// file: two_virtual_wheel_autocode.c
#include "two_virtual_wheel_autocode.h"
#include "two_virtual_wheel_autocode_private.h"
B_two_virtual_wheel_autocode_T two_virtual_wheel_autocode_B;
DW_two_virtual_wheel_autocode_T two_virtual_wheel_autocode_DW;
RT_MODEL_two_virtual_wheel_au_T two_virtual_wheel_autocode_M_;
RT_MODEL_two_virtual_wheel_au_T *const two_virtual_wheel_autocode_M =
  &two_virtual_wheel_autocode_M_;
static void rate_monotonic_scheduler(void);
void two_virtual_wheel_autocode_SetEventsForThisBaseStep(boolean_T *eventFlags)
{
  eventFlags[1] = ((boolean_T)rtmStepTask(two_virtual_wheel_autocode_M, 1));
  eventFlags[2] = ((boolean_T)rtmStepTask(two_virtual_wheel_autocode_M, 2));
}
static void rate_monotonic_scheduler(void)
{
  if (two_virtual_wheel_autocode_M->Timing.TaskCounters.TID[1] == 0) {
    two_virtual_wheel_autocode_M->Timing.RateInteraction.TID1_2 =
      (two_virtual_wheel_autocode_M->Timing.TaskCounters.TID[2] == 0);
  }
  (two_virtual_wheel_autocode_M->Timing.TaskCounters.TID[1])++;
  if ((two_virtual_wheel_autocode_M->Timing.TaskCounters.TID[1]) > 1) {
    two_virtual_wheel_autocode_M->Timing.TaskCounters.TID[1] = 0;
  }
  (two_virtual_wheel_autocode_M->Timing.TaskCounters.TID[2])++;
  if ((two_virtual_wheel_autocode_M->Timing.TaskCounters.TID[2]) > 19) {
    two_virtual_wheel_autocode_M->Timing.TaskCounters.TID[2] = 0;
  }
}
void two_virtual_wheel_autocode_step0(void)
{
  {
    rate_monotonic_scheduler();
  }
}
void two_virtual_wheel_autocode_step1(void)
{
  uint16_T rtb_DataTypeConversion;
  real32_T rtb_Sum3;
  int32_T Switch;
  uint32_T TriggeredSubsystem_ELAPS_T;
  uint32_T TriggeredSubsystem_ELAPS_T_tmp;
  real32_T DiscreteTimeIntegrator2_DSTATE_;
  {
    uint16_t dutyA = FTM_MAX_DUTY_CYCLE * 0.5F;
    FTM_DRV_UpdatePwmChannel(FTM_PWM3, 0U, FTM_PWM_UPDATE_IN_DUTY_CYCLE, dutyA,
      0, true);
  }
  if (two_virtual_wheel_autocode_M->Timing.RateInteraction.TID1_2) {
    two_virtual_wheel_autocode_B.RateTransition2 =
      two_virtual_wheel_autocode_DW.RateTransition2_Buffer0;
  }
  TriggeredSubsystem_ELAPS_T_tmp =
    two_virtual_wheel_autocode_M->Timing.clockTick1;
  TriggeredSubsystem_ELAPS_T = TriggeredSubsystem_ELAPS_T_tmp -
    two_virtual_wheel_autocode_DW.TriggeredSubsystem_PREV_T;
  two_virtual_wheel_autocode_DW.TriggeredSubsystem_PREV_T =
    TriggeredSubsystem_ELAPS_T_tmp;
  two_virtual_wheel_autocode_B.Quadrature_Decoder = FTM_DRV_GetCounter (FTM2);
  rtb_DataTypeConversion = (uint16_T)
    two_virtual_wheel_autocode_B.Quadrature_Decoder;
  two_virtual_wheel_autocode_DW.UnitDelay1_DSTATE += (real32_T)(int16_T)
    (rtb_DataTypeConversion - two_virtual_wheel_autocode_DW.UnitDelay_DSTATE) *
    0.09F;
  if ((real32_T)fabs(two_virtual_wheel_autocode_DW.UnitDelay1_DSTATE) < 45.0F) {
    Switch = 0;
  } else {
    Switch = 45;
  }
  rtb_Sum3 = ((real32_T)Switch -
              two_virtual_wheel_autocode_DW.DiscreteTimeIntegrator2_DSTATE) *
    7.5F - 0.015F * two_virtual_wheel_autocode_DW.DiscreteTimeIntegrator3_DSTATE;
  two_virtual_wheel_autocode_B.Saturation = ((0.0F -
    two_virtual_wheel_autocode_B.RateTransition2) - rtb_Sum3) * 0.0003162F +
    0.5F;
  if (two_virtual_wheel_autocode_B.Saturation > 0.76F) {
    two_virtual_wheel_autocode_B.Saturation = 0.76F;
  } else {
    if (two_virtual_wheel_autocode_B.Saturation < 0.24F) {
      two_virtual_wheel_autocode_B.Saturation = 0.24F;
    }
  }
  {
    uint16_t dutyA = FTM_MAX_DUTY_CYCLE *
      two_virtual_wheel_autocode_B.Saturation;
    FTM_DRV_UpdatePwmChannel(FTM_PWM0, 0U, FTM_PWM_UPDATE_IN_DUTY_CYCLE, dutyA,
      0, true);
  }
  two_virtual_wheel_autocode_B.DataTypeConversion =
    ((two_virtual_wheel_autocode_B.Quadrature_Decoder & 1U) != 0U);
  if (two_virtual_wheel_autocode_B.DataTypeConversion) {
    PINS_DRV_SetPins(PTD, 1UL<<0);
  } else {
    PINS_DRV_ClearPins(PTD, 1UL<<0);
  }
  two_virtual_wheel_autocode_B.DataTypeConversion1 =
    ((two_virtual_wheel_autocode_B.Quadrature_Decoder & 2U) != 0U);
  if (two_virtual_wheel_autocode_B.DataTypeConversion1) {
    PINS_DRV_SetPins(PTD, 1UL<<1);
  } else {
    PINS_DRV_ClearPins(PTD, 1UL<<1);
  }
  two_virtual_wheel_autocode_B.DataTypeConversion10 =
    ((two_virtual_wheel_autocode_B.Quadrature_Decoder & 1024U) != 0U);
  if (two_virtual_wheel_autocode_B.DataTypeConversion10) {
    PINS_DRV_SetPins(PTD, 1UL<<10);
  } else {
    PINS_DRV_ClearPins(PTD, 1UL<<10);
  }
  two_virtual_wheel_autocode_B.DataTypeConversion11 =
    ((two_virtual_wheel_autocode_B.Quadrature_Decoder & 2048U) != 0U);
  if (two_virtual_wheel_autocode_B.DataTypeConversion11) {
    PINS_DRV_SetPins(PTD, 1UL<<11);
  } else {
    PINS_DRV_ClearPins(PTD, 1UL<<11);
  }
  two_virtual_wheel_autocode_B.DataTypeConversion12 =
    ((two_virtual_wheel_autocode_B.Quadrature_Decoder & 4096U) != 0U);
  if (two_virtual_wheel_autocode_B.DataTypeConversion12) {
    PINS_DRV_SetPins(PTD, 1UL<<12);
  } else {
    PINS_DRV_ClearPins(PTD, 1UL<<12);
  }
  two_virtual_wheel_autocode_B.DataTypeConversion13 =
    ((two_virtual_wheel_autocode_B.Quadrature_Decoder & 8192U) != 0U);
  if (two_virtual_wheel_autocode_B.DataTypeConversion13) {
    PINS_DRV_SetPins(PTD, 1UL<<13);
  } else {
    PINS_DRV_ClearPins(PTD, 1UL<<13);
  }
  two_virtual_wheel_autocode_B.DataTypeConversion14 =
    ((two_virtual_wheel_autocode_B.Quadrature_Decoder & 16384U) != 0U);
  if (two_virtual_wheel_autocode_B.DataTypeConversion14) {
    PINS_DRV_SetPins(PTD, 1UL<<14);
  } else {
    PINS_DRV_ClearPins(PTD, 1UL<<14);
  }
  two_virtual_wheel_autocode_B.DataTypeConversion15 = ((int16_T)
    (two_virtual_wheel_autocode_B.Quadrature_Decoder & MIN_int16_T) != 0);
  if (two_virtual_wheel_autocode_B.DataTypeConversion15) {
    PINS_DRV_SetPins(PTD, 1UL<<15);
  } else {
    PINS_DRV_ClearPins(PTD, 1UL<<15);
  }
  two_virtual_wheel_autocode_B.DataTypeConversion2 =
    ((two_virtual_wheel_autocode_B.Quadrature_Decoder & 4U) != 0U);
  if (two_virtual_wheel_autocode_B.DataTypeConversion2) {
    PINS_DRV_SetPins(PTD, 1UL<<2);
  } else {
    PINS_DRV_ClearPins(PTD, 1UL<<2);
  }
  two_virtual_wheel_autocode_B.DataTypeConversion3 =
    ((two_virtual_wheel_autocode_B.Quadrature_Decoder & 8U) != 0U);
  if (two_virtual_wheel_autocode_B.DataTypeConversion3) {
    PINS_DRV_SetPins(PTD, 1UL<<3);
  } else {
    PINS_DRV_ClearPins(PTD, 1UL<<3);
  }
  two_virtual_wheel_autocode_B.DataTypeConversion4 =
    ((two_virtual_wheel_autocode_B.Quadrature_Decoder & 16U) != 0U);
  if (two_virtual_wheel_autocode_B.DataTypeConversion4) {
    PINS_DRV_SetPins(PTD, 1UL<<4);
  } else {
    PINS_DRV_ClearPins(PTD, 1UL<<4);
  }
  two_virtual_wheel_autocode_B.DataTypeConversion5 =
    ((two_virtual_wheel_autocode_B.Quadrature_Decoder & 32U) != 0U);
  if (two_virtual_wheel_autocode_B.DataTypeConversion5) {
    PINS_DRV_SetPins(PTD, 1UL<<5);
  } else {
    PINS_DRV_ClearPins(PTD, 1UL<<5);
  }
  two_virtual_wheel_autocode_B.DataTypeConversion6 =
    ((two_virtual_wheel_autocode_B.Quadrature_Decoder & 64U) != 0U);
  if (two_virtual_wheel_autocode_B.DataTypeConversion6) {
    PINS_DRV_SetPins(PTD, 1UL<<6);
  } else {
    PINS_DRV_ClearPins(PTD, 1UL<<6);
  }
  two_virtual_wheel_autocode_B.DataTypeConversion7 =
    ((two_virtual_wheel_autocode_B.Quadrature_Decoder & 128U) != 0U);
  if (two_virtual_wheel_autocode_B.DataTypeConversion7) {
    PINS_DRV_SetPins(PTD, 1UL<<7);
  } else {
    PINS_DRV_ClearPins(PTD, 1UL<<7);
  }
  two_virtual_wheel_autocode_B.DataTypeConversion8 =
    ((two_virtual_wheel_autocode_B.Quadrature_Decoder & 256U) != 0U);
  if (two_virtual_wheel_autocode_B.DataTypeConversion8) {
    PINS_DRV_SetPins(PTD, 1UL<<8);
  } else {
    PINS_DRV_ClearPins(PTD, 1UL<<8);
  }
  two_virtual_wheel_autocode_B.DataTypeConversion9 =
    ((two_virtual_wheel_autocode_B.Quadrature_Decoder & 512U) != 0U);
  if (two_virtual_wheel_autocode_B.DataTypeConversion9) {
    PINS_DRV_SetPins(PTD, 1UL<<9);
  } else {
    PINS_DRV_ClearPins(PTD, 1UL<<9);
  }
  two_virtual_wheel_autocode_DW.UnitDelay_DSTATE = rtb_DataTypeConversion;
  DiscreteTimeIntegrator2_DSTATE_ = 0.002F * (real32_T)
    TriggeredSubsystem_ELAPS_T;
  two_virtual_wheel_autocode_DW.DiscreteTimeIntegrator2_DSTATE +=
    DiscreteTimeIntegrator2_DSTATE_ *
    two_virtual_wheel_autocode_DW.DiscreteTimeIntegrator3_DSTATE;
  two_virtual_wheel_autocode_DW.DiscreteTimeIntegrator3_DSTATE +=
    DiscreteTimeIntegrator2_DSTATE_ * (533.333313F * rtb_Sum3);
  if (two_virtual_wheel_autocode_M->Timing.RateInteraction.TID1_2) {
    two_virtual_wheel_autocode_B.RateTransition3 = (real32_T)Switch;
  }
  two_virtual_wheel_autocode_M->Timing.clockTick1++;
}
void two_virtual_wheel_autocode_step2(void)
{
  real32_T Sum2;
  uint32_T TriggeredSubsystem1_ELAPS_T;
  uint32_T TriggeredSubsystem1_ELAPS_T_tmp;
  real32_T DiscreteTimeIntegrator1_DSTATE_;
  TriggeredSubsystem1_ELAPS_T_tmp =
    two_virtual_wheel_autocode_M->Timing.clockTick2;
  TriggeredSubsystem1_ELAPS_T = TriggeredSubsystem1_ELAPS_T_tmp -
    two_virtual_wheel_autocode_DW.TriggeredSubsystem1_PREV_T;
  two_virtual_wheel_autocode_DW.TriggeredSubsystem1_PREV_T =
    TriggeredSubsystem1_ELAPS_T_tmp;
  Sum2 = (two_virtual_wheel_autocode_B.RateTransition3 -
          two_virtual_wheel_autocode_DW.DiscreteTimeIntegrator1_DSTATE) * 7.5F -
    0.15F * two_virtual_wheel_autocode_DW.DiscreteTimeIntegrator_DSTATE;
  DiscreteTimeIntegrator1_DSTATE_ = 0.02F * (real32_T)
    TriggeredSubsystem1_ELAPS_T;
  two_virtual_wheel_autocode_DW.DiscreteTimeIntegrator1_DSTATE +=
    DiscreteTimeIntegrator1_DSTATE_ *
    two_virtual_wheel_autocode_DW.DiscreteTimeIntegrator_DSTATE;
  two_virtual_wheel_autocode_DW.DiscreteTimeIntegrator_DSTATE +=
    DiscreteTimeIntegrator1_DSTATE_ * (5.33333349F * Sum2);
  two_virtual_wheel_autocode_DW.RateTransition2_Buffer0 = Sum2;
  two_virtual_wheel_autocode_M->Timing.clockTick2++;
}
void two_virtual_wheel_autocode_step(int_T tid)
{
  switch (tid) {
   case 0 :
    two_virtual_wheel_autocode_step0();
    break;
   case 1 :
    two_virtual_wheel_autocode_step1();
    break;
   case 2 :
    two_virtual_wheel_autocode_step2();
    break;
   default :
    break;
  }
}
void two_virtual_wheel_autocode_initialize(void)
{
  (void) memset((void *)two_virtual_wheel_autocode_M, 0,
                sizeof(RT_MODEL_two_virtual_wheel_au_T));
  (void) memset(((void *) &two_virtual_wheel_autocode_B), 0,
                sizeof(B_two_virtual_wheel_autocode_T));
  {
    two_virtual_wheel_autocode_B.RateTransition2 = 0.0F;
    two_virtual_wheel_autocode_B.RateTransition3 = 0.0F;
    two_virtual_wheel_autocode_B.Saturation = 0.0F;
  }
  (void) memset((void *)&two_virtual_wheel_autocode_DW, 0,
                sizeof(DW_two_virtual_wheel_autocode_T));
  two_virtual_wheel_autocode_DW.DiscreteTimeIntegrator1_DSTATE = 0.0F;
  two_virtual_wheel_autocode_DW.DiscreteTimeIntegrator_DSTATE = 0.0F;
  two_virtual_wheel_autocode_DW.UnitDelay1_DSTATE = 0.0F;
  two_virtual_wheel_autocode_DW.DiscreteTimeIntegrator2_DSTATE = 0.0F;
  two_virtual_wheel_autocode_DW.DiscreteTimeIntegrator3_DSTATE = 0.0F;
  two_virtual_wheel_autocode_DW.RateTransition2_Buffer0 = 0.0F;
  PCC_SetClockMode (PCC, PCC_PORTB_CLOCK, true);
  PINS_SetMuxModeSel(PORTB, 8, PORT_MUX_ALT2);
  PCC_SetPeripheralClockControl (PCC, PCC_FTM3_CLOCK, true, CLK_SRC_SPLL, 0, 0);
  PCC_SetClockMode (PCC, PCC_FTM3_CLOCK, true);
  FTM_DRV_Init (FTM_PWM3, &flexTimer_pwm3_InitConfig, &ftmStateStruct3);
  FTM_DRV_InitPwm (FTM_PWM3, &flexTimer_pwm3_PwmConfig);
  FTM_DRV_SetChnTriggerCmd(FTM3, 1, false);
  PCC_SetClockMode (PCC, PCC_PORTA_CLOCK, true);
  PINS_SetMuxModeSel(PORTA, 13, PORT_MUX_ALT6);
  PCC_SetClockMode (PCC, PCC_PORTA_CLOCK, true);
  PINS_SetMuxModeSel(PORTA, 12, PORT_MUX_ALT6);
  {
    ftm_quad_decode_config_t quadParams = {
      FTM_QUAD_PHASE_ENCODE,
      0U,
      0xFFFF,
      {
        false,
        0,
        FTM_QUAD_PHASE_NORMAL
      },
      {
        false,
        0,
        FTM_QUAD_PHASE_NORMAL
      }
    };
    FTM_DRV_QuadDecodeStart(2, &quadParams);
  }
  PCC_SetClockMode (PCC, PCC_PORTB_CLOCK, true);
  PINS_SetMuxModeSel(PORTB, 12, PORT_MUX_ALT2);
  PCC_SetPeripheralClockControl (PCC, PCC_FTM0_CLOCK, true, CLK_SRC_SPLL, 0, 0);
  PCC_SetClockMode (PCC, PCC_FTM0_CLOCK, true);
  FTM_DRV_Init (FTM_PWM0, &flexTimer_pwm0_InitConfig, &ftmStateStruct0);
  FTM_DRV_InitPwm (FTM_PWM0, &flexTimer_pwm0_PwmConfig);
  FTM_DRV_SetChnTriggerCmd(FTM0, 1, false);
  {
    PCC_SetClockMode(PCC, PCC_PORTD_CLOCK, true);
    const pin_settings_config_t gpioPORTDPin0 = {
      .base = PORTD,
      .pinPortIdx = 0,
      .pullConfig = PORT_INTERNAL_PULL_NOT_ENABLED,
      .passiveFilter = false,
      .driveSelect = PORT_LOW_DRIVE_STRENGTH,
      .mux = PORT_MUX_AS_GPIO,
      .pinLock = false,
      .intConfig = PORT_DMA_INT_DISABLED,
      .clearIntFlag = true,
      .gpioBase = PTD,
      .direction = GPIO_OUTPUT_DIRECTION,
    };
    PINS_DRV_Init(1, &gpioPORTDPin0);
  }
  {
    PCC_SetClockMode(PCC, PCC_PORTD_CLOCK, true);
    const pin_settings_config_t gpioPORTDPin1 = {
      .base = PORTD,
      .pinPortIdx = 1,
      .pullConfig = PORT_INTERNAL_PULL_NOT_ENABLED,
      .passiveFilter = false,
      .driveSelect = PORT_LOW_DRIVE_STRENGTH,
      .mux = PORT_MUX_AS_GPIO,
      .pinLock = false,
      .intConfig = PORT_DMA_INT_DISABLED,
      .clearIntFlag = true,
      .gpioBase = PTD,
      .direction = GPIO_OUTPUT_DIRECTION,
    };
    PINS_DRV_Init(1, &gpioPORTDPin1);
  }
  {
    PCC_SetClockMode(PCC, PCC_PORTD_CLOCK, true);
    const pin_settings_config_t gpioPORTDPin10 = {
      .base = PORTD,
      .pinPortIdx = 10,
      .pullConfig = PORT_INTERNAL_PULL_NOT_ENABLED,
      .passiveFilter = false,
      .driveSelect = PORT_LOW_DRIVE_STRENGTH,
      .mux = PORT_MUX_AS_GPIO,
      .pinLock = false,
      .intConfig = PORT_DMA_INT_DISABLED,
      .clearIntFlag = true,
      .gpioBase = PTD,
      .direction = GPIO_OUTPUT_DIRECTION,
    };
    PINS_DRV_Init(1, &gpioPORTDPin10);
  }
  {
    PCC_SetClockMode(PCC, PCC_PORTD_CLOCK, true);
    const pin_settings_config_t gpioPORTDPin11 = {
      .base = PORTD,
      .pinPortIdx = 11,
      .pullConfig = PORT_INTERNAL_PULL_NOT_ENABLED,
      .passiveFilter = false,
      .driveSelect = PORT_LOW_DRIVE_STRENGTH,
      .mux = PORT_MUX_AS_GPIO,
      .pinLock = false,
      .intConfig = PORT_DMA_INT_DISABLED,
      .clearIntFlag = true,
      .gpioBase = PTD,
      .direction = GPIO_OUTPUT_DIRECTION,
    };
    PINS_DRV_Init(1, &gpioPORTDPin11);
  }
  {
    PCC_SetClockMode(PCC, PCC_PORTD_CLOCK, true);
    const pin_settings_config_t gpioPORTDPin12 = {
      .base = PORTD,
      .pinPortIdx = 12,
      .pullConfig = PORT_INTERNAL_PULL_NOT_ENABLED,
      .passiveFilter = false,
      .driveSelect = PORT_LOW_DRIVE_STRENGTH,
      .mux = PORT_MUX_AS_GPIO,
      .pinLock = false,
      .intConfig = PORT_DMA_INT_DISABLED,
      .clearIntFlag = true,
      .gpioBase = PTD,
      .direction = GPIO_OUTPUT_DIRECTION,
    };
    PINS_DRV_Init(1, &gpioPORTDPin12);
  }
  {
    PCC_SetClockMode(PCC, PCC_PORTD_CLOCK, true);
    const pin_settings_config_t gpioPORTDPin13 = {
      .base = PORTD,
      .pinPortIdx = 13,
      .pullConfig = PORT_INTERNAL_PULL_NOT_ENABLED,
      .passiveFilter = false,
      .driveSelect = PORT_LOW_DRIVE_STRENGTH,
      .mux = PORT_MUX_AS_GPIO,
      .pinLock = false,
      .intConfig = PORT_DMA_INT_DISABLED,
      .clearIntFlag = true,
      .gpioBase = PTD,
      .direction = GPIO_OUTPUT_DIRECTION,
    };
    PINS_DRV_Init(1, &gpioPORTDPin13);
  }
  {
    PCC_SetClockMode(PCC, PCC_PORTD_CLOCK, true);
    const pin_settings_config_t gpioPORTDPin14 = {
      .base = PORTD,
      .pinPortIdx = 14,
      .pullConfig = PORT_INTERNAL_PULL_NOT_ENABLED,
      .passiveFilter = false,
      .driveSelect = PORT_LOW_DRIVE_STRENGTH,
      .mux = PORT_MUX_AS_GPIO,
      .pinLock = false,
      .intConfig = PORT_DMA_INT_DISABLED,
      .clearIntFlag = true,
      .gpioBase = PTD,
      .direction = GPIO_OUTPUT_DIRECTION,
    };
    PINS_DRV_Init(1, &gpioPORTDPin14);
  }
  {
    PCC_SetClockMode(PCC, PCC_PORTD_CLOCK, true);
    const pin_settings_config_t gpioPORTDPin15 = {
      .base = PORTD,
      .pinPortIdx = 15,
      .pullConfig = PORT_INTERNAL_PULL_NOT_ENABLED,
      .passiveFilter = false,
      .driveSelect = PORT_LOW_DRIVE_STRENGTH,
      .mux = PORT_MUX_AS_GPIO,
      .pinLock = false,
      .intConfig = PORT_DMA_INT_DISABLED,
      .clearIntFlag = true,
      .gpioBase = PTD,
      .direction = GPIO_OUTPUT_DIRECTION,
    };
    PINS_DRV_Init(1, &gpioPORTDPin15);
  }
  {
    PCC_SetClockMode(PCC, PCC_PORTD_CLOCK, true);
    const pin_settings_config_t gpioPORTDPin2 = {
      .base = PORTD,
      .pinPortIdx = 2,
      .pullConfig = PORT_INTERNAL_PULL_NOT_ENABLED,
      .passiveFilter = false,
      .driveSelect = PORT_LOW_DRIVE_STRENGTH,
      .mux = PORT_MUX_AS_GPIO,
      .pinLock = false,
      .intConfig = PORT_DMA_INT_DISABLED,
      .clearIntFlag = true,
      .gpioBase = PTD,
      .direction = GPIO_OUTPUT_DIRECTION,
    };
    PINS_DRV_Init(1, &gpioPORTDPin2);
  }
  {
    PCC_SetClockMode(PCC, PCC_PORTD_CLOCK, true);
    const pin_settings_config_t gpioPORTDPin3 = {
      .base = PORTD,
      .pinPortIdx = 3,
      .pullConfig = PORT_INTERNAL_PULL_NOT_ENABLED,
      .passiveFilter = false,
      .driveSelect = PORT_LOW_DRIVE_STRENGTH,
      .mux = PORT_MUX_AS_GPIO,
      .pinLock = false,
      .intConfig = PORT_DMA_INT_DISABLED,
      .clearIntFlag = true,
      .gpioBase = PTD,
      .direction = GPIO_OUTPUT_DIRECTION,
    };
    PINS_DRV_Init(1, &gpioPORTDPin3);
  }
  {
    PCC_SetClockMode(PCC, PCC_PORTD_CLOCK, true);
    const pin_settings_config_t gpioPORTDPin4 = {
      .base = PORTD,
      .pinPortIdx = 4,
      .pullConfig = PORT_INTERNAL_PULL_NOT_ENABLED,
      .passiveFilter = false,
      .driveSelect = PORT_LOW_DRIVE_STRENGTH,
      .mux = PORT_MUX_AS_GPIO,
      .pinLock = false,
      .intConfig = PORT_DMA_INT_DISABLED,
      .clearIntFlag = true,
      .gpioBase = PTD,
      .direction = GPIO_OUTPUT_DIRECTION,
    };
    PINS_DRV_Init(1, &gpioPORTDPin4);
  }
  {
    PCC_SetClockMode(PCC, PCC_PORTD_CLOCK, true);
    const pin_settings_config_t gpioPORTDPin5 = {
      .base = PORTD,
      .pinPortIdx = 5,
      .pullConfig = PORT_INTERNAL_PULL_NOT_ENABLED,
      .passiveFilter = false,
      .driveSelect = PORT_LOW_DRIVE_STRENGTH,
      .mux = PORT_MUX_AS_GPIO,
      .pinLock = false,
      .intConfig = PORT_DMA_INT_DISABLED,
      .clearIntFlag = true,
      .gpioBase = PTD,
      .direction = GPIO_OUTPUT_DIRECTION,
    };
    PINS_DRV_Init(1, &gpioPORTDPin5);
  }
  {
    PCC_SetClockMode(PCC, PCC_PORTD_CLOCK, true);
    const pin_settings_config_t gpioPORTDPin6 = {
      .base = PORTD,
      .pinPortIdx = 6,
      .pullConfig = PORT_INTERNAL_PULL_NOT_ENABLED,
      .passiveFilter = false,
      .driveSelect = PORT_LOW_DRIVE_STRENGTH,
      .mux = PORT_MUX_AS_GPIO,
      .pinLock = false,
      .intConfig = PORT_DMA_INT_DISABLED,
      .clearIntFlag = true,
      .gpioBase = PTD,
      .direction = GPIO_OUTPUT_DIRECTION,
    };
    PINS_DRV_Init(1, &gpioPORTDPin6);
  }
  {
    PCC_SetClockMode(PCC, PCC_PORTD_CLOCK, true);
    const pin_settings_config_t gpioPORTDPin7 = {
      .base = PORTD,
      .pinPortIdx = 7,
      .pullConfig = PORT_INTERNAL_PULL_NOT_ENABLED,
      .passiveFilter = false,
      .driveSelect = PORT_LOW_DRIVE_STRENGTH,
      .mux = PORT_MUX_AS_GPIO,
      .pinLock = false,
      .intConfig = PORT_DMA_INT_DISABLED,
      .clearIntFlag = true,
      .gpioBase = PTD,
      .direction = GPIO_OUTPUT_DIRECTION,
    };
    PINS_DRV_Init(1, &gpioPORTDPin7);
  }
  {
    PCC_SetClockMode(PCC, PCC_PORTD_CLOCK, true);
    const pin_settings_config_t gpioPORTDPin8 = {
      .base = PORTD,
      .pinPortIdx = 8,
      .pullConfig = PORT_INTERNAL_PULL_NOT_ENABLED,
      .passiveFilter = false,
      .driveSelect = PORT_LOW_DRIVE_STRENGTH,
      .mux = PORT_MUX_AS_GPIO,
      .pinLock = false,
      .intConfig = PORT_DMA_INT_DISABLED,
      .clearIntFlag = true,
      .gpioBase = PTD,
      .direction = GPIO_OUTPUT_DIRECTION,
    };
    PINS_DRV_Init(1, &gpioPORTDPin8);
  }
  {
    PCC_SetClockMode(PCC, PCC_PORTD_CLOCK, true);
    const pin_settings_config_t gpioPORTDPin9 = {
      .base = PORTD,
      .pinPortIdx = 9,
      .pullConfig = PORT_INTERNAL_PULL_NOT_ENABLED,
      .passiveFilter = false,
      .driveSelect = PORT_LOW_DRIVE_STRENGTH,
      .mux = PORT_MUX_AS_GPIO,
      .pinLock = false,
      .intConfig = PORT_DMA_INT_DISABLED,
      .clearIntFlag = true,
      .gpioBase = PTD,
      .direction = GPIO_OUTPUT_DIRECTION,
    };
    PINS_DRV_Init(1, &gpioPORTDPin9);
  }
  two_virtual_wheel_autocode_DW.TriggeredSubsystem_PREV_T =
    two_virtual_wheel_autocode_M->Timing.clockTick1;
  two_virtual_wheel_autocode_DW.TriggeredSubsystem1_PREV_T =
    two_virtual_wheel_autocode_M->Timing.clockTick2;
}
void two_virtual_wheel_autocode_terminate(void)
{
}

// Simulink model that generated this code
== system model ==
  FTM_PWM_Config#1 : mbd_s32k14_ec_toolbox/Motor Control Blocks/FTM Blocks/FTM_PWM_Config  <- 1: Constant#1, 2: Constant#2
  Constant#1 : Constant  Value=0.5
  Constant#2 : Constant  Value=0
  MBD_S32K14x_Config_Information#1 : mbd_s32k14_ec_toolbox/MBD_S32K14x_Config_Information
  RateTransition2 : RateTransition  <- 1: TriggeredSubsystem1
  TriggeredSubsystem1 : Subsystem  <- 1: RateTransition3, Trigger: FunctionCallGenerator#1
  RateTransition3 : RateTransition  <- 1: TriggeredSubsystem
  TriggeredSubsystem : Subsystem  <- 1: RateTransition2, Trigger: FunctionCallGenerator#2
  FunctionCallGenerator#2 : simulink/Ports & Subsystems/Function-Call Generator
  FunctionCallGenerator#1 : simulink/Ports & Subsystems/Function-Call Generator
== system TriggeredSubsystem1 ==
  Inport#1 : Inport
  TriggerPort#1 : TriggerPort  TriggerType=function-call
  Outport#1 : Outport  <- 1: Sum2
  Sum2 : Sum  Inputs=+-  <- 1: Gain#1, 2: Gain#2
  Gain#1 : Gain  Gain=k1  <- 1: Sum#1
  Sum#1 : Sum  Inputs=+-  <- 1: Inport#1, 2: DiscreteTimeIntegrator1
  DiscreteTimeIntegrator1 : DiscreteIntegrator  <- 1: DiscreteTimeIntegrator
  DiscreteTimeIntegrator : DiscreteIntegrator  <- 1: Gain#3
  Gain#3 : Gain  Gain=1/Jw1  <- 1: Sum2
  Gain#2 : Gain  Gain=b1  <- 1: DiscreteTimeIntegrator
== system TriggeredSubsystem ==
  Inport#2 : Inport
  TriggerPort#2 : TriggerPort  TriggerType=function-call
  Outport#2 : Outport  <- 1: Switch
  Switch : Switch  Threshold=0.5  <- 1: Constant#3, 2: RelationalOperator#1, 3: Constant#4
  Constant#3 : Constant  Value=0
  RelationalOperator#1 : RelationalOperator  Operator=<  <- 1: Abs#1, 2: Constant#5
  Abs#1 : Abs  <- 1: Sum#2
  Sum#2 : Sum  Inputs=++  <- 1: Gain#4, 2: UnitDelay1
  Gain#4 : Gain  Gain=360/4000  <- 1: DataTypeConversion2
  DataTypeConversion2 : DataTypeConversion  <- 1: DataTypeConversion1
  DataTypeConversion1 : DataTypeConversion  <- 1: Sum#3
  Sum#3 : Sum  Inputs=+-  <- 1: DataTypeConversion, 2: UnitDelay
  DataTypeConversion : DataTypeConversion  <- 1: Quadrature_Decoder
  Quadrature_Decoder : mbd_s32k14_ec_toolbox/Motor Control Blocks/FTM Blocks/Quadrature_Decoder
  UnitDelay : UnitDelay  <- 1: DataTypeConversion
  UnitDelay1 : UnitDelay  <- 1: Sum#2
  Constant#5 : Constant  Value=45
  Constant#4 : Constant  Value=45
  FTM_PWM_Config#2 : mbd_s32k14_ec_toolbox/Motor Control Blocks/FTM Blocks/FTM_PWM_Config  <- 1: Saturation, 2: Constant#6
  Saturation : Saturate  UpperLimit=0.76  LowerLimit=0.24  <- 1: Sum#4
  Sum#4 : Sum  Inputs=++  <- 1: Gain#5, 2: Constant#7
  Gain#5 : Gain  Gain=3.162e-4  <- 1: DataTypeConversion#1
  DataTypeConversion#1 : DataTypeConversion  <- 1: Sum#5
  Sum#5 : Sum  Inputs=--  <- 1: Inport#2, 2: Sum3
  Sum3 : Sum  Inputs=+-  <- 1: Gain#6, 2: Gain#7
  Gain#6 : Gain  Gain=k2  <- 1: Sum#6
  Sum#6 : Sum  Inputs=+-  <- 1: Switch, 2: DiscreteTimeIntegrator2
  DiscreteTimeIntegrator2 : DiscreteIntegrator  <- 1: DiscreteTimeIntegrator3
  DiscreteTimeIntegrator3 : DiscreteIntegrator  <- 1: Gain#8
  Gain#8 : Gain  Gain=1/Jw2  <- 1: Sum3
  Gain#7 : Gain  Gain=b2  <- 1: DiscreteTimeIntegrator3
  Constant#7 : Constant  Value=0.5
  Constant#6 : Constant  Value=0
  Digital_Output#1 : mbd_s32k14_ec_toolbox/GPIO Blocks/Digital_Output  <- 1: DataTypeConversion#2
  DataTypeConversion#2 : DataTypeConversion  <- 1: BitwiseOperator#1
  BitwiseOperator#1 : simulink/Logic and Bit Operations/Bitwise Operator  logicop=AND  BitMask=1  <- 1: DataTypeConversion#3
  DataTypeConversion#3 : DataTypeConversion  <- 1: Quadrature_Decoder
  Digital_Output#2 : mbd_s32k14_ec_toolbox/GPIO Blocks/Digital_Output  <- 1: DataTypeConversion#4
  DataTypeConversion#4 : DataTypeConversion  <- 1: BitwiseOperator#2
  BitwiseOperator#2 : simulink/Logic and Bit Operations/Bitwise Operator  logicop=AND  BitMask=2  <- 1: DataTypeConversion#3
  Digital_Output#3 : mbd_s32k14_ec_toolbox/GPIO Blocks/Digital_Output  <- 1: DataTypeConversion10
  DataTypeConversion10 : DataTypeConversion  <- 1: BitwiseOperator#3
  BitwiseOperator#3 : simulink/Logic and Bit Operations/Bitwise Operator  logicop=AND  BitMask=1024  <- 1: DataTypeConversion#3
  Digital_Output#4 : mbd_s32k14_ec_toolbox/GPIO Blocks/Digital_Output  <- 1: DataTypeConversion11
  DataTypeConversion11 : DataTypeConversion  <- 1: BitwiseOperator#4
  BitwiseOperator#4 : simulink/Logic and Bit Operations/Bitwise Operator  logicop=AND  BitMask=2048  <- 1: DataTypeConversion#3
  Digital_Output#5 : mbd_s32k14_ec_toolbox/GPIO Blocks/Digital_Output  <- 1: DataTypeConversion12
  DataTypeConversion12 : DataTypeConversion  <- 1: BitwiseOperator#5
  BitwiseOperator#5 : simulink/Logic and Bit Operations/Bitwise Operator  logicop=AND  BitMask=4096  <- 1: DataTypeConversion#3
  Digital_Output#6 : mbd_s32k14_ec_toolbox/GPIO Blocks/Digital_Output  <- 1: DataTypeConversion13
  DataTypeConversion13 : DataTypeConversion  <- 1: BitwiseOperator#6
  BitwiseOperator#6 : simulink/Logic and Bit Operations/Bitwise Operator  logicop=AND  BitMask=8192  <- 1: DataTypeConversion#3
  Digital_Output#7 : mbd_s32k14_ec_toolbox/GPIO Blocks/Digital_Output  <- 1: DataTypeConversion14
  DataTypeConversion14 : DataTypeConversion  <- 1: BitwiseOperator#7
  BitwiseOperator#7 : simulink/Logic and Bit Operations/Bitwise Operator  logicop=AND  BitMask=16384  <- 1: DataTypeConversion#3
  Digital_Output#8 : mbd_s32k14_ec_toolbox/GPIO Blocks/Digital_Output  <- 1: DataTypeConversion15
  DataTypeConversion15 : DataTypeConversion  <- 1: BitwiseOperator#8
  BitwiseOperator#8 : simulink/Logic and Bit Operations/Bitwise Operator  logicop=AND  BitMask=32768  <- 1: DataTypeConversion#3
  Digital_Output#9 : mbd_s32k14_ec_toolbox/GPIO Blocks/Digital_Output  <- 1: DataTypeConversion#5
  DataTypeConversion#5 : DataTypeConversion  <- 1: BitwiseOperator#9
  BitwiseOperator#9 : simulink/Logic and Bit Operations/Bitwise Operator  logicop=AND  BitMask=4  <- 1: DataTypeConversion#3
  Digital_Output#10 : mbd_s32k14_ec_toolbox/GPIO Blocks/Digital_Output  <- 1: DataTypeConversion3
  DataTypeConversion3 : DataTypeConversion  <- 1: BitwiseOperator#10
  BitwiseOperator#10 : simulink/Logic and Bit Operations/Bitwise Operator  logicop=AND  BitMask=8  <- 1: DataTypeConversion#3
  Digital_Output#11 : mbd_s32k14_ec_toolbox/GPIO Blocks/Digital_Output  <- 1: DataTypeConversion4
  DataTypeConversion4 : DataTypeConversion  <- 1: BitwiseOperator#11
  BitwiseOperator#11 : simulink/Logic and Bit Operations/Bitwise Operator  logicop=AND  BitMask=16  <- 1: DataTypeConversion#3
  Digital_Output#12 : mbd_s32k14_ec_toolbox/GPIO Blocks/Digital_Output  <- 1: DataTypeConversion5
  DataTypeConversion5 : DataTypeConversion  <- 1: BitwiseOperator#12
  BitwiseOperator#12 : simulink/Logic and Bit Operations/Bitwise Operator  logicop=AND  BitMask=32  <- 1: DataTypeConversion#3
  Digital_Output#13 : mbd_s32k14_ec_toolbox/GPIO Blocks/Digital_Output  <- 1: DataTypeConversion6
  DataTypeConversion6 : DataTypeConversion  <- 1: BitwiseOperator#13
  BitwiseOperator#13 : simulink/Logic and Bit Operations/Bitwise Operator  logicop=AND  BitMask=64  <- 1: DataTypeConversion#3
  Digital_Output#14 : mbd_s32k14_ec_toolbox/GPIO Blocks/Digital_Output  <- 1: DataTypeConversion7
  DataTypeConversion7 : DataTypeConversion  <- 1: BitwiseOperator#14
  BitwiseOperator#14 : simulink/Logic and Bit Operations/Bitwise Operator  logicop=AND  BitMask=128  <- 1: DataTypeConversion#3
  Digital_Output#15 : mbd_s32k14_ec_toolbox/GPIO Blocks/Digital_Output  <- 1: DataTypeConversion8
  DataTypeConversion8 : DataTypeConversion  <- 1: BitwiseOperator#15
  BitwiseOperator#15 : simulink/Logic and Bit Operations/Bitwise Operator  logicop=AND  BitMask=256  <- 1: DataTypeConversion#3
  Digital_Output#16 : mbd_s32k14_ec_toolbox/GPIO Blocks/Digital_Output  <- 1: DataTypeConversion9
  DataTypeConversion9 : DataTypeConversion  <- 1: BitwiseOperator#16
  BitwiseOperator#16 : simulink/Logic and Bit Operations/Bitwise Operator  logicop=AND  BitMask=512  <- 1: DataTypeConversion#3
